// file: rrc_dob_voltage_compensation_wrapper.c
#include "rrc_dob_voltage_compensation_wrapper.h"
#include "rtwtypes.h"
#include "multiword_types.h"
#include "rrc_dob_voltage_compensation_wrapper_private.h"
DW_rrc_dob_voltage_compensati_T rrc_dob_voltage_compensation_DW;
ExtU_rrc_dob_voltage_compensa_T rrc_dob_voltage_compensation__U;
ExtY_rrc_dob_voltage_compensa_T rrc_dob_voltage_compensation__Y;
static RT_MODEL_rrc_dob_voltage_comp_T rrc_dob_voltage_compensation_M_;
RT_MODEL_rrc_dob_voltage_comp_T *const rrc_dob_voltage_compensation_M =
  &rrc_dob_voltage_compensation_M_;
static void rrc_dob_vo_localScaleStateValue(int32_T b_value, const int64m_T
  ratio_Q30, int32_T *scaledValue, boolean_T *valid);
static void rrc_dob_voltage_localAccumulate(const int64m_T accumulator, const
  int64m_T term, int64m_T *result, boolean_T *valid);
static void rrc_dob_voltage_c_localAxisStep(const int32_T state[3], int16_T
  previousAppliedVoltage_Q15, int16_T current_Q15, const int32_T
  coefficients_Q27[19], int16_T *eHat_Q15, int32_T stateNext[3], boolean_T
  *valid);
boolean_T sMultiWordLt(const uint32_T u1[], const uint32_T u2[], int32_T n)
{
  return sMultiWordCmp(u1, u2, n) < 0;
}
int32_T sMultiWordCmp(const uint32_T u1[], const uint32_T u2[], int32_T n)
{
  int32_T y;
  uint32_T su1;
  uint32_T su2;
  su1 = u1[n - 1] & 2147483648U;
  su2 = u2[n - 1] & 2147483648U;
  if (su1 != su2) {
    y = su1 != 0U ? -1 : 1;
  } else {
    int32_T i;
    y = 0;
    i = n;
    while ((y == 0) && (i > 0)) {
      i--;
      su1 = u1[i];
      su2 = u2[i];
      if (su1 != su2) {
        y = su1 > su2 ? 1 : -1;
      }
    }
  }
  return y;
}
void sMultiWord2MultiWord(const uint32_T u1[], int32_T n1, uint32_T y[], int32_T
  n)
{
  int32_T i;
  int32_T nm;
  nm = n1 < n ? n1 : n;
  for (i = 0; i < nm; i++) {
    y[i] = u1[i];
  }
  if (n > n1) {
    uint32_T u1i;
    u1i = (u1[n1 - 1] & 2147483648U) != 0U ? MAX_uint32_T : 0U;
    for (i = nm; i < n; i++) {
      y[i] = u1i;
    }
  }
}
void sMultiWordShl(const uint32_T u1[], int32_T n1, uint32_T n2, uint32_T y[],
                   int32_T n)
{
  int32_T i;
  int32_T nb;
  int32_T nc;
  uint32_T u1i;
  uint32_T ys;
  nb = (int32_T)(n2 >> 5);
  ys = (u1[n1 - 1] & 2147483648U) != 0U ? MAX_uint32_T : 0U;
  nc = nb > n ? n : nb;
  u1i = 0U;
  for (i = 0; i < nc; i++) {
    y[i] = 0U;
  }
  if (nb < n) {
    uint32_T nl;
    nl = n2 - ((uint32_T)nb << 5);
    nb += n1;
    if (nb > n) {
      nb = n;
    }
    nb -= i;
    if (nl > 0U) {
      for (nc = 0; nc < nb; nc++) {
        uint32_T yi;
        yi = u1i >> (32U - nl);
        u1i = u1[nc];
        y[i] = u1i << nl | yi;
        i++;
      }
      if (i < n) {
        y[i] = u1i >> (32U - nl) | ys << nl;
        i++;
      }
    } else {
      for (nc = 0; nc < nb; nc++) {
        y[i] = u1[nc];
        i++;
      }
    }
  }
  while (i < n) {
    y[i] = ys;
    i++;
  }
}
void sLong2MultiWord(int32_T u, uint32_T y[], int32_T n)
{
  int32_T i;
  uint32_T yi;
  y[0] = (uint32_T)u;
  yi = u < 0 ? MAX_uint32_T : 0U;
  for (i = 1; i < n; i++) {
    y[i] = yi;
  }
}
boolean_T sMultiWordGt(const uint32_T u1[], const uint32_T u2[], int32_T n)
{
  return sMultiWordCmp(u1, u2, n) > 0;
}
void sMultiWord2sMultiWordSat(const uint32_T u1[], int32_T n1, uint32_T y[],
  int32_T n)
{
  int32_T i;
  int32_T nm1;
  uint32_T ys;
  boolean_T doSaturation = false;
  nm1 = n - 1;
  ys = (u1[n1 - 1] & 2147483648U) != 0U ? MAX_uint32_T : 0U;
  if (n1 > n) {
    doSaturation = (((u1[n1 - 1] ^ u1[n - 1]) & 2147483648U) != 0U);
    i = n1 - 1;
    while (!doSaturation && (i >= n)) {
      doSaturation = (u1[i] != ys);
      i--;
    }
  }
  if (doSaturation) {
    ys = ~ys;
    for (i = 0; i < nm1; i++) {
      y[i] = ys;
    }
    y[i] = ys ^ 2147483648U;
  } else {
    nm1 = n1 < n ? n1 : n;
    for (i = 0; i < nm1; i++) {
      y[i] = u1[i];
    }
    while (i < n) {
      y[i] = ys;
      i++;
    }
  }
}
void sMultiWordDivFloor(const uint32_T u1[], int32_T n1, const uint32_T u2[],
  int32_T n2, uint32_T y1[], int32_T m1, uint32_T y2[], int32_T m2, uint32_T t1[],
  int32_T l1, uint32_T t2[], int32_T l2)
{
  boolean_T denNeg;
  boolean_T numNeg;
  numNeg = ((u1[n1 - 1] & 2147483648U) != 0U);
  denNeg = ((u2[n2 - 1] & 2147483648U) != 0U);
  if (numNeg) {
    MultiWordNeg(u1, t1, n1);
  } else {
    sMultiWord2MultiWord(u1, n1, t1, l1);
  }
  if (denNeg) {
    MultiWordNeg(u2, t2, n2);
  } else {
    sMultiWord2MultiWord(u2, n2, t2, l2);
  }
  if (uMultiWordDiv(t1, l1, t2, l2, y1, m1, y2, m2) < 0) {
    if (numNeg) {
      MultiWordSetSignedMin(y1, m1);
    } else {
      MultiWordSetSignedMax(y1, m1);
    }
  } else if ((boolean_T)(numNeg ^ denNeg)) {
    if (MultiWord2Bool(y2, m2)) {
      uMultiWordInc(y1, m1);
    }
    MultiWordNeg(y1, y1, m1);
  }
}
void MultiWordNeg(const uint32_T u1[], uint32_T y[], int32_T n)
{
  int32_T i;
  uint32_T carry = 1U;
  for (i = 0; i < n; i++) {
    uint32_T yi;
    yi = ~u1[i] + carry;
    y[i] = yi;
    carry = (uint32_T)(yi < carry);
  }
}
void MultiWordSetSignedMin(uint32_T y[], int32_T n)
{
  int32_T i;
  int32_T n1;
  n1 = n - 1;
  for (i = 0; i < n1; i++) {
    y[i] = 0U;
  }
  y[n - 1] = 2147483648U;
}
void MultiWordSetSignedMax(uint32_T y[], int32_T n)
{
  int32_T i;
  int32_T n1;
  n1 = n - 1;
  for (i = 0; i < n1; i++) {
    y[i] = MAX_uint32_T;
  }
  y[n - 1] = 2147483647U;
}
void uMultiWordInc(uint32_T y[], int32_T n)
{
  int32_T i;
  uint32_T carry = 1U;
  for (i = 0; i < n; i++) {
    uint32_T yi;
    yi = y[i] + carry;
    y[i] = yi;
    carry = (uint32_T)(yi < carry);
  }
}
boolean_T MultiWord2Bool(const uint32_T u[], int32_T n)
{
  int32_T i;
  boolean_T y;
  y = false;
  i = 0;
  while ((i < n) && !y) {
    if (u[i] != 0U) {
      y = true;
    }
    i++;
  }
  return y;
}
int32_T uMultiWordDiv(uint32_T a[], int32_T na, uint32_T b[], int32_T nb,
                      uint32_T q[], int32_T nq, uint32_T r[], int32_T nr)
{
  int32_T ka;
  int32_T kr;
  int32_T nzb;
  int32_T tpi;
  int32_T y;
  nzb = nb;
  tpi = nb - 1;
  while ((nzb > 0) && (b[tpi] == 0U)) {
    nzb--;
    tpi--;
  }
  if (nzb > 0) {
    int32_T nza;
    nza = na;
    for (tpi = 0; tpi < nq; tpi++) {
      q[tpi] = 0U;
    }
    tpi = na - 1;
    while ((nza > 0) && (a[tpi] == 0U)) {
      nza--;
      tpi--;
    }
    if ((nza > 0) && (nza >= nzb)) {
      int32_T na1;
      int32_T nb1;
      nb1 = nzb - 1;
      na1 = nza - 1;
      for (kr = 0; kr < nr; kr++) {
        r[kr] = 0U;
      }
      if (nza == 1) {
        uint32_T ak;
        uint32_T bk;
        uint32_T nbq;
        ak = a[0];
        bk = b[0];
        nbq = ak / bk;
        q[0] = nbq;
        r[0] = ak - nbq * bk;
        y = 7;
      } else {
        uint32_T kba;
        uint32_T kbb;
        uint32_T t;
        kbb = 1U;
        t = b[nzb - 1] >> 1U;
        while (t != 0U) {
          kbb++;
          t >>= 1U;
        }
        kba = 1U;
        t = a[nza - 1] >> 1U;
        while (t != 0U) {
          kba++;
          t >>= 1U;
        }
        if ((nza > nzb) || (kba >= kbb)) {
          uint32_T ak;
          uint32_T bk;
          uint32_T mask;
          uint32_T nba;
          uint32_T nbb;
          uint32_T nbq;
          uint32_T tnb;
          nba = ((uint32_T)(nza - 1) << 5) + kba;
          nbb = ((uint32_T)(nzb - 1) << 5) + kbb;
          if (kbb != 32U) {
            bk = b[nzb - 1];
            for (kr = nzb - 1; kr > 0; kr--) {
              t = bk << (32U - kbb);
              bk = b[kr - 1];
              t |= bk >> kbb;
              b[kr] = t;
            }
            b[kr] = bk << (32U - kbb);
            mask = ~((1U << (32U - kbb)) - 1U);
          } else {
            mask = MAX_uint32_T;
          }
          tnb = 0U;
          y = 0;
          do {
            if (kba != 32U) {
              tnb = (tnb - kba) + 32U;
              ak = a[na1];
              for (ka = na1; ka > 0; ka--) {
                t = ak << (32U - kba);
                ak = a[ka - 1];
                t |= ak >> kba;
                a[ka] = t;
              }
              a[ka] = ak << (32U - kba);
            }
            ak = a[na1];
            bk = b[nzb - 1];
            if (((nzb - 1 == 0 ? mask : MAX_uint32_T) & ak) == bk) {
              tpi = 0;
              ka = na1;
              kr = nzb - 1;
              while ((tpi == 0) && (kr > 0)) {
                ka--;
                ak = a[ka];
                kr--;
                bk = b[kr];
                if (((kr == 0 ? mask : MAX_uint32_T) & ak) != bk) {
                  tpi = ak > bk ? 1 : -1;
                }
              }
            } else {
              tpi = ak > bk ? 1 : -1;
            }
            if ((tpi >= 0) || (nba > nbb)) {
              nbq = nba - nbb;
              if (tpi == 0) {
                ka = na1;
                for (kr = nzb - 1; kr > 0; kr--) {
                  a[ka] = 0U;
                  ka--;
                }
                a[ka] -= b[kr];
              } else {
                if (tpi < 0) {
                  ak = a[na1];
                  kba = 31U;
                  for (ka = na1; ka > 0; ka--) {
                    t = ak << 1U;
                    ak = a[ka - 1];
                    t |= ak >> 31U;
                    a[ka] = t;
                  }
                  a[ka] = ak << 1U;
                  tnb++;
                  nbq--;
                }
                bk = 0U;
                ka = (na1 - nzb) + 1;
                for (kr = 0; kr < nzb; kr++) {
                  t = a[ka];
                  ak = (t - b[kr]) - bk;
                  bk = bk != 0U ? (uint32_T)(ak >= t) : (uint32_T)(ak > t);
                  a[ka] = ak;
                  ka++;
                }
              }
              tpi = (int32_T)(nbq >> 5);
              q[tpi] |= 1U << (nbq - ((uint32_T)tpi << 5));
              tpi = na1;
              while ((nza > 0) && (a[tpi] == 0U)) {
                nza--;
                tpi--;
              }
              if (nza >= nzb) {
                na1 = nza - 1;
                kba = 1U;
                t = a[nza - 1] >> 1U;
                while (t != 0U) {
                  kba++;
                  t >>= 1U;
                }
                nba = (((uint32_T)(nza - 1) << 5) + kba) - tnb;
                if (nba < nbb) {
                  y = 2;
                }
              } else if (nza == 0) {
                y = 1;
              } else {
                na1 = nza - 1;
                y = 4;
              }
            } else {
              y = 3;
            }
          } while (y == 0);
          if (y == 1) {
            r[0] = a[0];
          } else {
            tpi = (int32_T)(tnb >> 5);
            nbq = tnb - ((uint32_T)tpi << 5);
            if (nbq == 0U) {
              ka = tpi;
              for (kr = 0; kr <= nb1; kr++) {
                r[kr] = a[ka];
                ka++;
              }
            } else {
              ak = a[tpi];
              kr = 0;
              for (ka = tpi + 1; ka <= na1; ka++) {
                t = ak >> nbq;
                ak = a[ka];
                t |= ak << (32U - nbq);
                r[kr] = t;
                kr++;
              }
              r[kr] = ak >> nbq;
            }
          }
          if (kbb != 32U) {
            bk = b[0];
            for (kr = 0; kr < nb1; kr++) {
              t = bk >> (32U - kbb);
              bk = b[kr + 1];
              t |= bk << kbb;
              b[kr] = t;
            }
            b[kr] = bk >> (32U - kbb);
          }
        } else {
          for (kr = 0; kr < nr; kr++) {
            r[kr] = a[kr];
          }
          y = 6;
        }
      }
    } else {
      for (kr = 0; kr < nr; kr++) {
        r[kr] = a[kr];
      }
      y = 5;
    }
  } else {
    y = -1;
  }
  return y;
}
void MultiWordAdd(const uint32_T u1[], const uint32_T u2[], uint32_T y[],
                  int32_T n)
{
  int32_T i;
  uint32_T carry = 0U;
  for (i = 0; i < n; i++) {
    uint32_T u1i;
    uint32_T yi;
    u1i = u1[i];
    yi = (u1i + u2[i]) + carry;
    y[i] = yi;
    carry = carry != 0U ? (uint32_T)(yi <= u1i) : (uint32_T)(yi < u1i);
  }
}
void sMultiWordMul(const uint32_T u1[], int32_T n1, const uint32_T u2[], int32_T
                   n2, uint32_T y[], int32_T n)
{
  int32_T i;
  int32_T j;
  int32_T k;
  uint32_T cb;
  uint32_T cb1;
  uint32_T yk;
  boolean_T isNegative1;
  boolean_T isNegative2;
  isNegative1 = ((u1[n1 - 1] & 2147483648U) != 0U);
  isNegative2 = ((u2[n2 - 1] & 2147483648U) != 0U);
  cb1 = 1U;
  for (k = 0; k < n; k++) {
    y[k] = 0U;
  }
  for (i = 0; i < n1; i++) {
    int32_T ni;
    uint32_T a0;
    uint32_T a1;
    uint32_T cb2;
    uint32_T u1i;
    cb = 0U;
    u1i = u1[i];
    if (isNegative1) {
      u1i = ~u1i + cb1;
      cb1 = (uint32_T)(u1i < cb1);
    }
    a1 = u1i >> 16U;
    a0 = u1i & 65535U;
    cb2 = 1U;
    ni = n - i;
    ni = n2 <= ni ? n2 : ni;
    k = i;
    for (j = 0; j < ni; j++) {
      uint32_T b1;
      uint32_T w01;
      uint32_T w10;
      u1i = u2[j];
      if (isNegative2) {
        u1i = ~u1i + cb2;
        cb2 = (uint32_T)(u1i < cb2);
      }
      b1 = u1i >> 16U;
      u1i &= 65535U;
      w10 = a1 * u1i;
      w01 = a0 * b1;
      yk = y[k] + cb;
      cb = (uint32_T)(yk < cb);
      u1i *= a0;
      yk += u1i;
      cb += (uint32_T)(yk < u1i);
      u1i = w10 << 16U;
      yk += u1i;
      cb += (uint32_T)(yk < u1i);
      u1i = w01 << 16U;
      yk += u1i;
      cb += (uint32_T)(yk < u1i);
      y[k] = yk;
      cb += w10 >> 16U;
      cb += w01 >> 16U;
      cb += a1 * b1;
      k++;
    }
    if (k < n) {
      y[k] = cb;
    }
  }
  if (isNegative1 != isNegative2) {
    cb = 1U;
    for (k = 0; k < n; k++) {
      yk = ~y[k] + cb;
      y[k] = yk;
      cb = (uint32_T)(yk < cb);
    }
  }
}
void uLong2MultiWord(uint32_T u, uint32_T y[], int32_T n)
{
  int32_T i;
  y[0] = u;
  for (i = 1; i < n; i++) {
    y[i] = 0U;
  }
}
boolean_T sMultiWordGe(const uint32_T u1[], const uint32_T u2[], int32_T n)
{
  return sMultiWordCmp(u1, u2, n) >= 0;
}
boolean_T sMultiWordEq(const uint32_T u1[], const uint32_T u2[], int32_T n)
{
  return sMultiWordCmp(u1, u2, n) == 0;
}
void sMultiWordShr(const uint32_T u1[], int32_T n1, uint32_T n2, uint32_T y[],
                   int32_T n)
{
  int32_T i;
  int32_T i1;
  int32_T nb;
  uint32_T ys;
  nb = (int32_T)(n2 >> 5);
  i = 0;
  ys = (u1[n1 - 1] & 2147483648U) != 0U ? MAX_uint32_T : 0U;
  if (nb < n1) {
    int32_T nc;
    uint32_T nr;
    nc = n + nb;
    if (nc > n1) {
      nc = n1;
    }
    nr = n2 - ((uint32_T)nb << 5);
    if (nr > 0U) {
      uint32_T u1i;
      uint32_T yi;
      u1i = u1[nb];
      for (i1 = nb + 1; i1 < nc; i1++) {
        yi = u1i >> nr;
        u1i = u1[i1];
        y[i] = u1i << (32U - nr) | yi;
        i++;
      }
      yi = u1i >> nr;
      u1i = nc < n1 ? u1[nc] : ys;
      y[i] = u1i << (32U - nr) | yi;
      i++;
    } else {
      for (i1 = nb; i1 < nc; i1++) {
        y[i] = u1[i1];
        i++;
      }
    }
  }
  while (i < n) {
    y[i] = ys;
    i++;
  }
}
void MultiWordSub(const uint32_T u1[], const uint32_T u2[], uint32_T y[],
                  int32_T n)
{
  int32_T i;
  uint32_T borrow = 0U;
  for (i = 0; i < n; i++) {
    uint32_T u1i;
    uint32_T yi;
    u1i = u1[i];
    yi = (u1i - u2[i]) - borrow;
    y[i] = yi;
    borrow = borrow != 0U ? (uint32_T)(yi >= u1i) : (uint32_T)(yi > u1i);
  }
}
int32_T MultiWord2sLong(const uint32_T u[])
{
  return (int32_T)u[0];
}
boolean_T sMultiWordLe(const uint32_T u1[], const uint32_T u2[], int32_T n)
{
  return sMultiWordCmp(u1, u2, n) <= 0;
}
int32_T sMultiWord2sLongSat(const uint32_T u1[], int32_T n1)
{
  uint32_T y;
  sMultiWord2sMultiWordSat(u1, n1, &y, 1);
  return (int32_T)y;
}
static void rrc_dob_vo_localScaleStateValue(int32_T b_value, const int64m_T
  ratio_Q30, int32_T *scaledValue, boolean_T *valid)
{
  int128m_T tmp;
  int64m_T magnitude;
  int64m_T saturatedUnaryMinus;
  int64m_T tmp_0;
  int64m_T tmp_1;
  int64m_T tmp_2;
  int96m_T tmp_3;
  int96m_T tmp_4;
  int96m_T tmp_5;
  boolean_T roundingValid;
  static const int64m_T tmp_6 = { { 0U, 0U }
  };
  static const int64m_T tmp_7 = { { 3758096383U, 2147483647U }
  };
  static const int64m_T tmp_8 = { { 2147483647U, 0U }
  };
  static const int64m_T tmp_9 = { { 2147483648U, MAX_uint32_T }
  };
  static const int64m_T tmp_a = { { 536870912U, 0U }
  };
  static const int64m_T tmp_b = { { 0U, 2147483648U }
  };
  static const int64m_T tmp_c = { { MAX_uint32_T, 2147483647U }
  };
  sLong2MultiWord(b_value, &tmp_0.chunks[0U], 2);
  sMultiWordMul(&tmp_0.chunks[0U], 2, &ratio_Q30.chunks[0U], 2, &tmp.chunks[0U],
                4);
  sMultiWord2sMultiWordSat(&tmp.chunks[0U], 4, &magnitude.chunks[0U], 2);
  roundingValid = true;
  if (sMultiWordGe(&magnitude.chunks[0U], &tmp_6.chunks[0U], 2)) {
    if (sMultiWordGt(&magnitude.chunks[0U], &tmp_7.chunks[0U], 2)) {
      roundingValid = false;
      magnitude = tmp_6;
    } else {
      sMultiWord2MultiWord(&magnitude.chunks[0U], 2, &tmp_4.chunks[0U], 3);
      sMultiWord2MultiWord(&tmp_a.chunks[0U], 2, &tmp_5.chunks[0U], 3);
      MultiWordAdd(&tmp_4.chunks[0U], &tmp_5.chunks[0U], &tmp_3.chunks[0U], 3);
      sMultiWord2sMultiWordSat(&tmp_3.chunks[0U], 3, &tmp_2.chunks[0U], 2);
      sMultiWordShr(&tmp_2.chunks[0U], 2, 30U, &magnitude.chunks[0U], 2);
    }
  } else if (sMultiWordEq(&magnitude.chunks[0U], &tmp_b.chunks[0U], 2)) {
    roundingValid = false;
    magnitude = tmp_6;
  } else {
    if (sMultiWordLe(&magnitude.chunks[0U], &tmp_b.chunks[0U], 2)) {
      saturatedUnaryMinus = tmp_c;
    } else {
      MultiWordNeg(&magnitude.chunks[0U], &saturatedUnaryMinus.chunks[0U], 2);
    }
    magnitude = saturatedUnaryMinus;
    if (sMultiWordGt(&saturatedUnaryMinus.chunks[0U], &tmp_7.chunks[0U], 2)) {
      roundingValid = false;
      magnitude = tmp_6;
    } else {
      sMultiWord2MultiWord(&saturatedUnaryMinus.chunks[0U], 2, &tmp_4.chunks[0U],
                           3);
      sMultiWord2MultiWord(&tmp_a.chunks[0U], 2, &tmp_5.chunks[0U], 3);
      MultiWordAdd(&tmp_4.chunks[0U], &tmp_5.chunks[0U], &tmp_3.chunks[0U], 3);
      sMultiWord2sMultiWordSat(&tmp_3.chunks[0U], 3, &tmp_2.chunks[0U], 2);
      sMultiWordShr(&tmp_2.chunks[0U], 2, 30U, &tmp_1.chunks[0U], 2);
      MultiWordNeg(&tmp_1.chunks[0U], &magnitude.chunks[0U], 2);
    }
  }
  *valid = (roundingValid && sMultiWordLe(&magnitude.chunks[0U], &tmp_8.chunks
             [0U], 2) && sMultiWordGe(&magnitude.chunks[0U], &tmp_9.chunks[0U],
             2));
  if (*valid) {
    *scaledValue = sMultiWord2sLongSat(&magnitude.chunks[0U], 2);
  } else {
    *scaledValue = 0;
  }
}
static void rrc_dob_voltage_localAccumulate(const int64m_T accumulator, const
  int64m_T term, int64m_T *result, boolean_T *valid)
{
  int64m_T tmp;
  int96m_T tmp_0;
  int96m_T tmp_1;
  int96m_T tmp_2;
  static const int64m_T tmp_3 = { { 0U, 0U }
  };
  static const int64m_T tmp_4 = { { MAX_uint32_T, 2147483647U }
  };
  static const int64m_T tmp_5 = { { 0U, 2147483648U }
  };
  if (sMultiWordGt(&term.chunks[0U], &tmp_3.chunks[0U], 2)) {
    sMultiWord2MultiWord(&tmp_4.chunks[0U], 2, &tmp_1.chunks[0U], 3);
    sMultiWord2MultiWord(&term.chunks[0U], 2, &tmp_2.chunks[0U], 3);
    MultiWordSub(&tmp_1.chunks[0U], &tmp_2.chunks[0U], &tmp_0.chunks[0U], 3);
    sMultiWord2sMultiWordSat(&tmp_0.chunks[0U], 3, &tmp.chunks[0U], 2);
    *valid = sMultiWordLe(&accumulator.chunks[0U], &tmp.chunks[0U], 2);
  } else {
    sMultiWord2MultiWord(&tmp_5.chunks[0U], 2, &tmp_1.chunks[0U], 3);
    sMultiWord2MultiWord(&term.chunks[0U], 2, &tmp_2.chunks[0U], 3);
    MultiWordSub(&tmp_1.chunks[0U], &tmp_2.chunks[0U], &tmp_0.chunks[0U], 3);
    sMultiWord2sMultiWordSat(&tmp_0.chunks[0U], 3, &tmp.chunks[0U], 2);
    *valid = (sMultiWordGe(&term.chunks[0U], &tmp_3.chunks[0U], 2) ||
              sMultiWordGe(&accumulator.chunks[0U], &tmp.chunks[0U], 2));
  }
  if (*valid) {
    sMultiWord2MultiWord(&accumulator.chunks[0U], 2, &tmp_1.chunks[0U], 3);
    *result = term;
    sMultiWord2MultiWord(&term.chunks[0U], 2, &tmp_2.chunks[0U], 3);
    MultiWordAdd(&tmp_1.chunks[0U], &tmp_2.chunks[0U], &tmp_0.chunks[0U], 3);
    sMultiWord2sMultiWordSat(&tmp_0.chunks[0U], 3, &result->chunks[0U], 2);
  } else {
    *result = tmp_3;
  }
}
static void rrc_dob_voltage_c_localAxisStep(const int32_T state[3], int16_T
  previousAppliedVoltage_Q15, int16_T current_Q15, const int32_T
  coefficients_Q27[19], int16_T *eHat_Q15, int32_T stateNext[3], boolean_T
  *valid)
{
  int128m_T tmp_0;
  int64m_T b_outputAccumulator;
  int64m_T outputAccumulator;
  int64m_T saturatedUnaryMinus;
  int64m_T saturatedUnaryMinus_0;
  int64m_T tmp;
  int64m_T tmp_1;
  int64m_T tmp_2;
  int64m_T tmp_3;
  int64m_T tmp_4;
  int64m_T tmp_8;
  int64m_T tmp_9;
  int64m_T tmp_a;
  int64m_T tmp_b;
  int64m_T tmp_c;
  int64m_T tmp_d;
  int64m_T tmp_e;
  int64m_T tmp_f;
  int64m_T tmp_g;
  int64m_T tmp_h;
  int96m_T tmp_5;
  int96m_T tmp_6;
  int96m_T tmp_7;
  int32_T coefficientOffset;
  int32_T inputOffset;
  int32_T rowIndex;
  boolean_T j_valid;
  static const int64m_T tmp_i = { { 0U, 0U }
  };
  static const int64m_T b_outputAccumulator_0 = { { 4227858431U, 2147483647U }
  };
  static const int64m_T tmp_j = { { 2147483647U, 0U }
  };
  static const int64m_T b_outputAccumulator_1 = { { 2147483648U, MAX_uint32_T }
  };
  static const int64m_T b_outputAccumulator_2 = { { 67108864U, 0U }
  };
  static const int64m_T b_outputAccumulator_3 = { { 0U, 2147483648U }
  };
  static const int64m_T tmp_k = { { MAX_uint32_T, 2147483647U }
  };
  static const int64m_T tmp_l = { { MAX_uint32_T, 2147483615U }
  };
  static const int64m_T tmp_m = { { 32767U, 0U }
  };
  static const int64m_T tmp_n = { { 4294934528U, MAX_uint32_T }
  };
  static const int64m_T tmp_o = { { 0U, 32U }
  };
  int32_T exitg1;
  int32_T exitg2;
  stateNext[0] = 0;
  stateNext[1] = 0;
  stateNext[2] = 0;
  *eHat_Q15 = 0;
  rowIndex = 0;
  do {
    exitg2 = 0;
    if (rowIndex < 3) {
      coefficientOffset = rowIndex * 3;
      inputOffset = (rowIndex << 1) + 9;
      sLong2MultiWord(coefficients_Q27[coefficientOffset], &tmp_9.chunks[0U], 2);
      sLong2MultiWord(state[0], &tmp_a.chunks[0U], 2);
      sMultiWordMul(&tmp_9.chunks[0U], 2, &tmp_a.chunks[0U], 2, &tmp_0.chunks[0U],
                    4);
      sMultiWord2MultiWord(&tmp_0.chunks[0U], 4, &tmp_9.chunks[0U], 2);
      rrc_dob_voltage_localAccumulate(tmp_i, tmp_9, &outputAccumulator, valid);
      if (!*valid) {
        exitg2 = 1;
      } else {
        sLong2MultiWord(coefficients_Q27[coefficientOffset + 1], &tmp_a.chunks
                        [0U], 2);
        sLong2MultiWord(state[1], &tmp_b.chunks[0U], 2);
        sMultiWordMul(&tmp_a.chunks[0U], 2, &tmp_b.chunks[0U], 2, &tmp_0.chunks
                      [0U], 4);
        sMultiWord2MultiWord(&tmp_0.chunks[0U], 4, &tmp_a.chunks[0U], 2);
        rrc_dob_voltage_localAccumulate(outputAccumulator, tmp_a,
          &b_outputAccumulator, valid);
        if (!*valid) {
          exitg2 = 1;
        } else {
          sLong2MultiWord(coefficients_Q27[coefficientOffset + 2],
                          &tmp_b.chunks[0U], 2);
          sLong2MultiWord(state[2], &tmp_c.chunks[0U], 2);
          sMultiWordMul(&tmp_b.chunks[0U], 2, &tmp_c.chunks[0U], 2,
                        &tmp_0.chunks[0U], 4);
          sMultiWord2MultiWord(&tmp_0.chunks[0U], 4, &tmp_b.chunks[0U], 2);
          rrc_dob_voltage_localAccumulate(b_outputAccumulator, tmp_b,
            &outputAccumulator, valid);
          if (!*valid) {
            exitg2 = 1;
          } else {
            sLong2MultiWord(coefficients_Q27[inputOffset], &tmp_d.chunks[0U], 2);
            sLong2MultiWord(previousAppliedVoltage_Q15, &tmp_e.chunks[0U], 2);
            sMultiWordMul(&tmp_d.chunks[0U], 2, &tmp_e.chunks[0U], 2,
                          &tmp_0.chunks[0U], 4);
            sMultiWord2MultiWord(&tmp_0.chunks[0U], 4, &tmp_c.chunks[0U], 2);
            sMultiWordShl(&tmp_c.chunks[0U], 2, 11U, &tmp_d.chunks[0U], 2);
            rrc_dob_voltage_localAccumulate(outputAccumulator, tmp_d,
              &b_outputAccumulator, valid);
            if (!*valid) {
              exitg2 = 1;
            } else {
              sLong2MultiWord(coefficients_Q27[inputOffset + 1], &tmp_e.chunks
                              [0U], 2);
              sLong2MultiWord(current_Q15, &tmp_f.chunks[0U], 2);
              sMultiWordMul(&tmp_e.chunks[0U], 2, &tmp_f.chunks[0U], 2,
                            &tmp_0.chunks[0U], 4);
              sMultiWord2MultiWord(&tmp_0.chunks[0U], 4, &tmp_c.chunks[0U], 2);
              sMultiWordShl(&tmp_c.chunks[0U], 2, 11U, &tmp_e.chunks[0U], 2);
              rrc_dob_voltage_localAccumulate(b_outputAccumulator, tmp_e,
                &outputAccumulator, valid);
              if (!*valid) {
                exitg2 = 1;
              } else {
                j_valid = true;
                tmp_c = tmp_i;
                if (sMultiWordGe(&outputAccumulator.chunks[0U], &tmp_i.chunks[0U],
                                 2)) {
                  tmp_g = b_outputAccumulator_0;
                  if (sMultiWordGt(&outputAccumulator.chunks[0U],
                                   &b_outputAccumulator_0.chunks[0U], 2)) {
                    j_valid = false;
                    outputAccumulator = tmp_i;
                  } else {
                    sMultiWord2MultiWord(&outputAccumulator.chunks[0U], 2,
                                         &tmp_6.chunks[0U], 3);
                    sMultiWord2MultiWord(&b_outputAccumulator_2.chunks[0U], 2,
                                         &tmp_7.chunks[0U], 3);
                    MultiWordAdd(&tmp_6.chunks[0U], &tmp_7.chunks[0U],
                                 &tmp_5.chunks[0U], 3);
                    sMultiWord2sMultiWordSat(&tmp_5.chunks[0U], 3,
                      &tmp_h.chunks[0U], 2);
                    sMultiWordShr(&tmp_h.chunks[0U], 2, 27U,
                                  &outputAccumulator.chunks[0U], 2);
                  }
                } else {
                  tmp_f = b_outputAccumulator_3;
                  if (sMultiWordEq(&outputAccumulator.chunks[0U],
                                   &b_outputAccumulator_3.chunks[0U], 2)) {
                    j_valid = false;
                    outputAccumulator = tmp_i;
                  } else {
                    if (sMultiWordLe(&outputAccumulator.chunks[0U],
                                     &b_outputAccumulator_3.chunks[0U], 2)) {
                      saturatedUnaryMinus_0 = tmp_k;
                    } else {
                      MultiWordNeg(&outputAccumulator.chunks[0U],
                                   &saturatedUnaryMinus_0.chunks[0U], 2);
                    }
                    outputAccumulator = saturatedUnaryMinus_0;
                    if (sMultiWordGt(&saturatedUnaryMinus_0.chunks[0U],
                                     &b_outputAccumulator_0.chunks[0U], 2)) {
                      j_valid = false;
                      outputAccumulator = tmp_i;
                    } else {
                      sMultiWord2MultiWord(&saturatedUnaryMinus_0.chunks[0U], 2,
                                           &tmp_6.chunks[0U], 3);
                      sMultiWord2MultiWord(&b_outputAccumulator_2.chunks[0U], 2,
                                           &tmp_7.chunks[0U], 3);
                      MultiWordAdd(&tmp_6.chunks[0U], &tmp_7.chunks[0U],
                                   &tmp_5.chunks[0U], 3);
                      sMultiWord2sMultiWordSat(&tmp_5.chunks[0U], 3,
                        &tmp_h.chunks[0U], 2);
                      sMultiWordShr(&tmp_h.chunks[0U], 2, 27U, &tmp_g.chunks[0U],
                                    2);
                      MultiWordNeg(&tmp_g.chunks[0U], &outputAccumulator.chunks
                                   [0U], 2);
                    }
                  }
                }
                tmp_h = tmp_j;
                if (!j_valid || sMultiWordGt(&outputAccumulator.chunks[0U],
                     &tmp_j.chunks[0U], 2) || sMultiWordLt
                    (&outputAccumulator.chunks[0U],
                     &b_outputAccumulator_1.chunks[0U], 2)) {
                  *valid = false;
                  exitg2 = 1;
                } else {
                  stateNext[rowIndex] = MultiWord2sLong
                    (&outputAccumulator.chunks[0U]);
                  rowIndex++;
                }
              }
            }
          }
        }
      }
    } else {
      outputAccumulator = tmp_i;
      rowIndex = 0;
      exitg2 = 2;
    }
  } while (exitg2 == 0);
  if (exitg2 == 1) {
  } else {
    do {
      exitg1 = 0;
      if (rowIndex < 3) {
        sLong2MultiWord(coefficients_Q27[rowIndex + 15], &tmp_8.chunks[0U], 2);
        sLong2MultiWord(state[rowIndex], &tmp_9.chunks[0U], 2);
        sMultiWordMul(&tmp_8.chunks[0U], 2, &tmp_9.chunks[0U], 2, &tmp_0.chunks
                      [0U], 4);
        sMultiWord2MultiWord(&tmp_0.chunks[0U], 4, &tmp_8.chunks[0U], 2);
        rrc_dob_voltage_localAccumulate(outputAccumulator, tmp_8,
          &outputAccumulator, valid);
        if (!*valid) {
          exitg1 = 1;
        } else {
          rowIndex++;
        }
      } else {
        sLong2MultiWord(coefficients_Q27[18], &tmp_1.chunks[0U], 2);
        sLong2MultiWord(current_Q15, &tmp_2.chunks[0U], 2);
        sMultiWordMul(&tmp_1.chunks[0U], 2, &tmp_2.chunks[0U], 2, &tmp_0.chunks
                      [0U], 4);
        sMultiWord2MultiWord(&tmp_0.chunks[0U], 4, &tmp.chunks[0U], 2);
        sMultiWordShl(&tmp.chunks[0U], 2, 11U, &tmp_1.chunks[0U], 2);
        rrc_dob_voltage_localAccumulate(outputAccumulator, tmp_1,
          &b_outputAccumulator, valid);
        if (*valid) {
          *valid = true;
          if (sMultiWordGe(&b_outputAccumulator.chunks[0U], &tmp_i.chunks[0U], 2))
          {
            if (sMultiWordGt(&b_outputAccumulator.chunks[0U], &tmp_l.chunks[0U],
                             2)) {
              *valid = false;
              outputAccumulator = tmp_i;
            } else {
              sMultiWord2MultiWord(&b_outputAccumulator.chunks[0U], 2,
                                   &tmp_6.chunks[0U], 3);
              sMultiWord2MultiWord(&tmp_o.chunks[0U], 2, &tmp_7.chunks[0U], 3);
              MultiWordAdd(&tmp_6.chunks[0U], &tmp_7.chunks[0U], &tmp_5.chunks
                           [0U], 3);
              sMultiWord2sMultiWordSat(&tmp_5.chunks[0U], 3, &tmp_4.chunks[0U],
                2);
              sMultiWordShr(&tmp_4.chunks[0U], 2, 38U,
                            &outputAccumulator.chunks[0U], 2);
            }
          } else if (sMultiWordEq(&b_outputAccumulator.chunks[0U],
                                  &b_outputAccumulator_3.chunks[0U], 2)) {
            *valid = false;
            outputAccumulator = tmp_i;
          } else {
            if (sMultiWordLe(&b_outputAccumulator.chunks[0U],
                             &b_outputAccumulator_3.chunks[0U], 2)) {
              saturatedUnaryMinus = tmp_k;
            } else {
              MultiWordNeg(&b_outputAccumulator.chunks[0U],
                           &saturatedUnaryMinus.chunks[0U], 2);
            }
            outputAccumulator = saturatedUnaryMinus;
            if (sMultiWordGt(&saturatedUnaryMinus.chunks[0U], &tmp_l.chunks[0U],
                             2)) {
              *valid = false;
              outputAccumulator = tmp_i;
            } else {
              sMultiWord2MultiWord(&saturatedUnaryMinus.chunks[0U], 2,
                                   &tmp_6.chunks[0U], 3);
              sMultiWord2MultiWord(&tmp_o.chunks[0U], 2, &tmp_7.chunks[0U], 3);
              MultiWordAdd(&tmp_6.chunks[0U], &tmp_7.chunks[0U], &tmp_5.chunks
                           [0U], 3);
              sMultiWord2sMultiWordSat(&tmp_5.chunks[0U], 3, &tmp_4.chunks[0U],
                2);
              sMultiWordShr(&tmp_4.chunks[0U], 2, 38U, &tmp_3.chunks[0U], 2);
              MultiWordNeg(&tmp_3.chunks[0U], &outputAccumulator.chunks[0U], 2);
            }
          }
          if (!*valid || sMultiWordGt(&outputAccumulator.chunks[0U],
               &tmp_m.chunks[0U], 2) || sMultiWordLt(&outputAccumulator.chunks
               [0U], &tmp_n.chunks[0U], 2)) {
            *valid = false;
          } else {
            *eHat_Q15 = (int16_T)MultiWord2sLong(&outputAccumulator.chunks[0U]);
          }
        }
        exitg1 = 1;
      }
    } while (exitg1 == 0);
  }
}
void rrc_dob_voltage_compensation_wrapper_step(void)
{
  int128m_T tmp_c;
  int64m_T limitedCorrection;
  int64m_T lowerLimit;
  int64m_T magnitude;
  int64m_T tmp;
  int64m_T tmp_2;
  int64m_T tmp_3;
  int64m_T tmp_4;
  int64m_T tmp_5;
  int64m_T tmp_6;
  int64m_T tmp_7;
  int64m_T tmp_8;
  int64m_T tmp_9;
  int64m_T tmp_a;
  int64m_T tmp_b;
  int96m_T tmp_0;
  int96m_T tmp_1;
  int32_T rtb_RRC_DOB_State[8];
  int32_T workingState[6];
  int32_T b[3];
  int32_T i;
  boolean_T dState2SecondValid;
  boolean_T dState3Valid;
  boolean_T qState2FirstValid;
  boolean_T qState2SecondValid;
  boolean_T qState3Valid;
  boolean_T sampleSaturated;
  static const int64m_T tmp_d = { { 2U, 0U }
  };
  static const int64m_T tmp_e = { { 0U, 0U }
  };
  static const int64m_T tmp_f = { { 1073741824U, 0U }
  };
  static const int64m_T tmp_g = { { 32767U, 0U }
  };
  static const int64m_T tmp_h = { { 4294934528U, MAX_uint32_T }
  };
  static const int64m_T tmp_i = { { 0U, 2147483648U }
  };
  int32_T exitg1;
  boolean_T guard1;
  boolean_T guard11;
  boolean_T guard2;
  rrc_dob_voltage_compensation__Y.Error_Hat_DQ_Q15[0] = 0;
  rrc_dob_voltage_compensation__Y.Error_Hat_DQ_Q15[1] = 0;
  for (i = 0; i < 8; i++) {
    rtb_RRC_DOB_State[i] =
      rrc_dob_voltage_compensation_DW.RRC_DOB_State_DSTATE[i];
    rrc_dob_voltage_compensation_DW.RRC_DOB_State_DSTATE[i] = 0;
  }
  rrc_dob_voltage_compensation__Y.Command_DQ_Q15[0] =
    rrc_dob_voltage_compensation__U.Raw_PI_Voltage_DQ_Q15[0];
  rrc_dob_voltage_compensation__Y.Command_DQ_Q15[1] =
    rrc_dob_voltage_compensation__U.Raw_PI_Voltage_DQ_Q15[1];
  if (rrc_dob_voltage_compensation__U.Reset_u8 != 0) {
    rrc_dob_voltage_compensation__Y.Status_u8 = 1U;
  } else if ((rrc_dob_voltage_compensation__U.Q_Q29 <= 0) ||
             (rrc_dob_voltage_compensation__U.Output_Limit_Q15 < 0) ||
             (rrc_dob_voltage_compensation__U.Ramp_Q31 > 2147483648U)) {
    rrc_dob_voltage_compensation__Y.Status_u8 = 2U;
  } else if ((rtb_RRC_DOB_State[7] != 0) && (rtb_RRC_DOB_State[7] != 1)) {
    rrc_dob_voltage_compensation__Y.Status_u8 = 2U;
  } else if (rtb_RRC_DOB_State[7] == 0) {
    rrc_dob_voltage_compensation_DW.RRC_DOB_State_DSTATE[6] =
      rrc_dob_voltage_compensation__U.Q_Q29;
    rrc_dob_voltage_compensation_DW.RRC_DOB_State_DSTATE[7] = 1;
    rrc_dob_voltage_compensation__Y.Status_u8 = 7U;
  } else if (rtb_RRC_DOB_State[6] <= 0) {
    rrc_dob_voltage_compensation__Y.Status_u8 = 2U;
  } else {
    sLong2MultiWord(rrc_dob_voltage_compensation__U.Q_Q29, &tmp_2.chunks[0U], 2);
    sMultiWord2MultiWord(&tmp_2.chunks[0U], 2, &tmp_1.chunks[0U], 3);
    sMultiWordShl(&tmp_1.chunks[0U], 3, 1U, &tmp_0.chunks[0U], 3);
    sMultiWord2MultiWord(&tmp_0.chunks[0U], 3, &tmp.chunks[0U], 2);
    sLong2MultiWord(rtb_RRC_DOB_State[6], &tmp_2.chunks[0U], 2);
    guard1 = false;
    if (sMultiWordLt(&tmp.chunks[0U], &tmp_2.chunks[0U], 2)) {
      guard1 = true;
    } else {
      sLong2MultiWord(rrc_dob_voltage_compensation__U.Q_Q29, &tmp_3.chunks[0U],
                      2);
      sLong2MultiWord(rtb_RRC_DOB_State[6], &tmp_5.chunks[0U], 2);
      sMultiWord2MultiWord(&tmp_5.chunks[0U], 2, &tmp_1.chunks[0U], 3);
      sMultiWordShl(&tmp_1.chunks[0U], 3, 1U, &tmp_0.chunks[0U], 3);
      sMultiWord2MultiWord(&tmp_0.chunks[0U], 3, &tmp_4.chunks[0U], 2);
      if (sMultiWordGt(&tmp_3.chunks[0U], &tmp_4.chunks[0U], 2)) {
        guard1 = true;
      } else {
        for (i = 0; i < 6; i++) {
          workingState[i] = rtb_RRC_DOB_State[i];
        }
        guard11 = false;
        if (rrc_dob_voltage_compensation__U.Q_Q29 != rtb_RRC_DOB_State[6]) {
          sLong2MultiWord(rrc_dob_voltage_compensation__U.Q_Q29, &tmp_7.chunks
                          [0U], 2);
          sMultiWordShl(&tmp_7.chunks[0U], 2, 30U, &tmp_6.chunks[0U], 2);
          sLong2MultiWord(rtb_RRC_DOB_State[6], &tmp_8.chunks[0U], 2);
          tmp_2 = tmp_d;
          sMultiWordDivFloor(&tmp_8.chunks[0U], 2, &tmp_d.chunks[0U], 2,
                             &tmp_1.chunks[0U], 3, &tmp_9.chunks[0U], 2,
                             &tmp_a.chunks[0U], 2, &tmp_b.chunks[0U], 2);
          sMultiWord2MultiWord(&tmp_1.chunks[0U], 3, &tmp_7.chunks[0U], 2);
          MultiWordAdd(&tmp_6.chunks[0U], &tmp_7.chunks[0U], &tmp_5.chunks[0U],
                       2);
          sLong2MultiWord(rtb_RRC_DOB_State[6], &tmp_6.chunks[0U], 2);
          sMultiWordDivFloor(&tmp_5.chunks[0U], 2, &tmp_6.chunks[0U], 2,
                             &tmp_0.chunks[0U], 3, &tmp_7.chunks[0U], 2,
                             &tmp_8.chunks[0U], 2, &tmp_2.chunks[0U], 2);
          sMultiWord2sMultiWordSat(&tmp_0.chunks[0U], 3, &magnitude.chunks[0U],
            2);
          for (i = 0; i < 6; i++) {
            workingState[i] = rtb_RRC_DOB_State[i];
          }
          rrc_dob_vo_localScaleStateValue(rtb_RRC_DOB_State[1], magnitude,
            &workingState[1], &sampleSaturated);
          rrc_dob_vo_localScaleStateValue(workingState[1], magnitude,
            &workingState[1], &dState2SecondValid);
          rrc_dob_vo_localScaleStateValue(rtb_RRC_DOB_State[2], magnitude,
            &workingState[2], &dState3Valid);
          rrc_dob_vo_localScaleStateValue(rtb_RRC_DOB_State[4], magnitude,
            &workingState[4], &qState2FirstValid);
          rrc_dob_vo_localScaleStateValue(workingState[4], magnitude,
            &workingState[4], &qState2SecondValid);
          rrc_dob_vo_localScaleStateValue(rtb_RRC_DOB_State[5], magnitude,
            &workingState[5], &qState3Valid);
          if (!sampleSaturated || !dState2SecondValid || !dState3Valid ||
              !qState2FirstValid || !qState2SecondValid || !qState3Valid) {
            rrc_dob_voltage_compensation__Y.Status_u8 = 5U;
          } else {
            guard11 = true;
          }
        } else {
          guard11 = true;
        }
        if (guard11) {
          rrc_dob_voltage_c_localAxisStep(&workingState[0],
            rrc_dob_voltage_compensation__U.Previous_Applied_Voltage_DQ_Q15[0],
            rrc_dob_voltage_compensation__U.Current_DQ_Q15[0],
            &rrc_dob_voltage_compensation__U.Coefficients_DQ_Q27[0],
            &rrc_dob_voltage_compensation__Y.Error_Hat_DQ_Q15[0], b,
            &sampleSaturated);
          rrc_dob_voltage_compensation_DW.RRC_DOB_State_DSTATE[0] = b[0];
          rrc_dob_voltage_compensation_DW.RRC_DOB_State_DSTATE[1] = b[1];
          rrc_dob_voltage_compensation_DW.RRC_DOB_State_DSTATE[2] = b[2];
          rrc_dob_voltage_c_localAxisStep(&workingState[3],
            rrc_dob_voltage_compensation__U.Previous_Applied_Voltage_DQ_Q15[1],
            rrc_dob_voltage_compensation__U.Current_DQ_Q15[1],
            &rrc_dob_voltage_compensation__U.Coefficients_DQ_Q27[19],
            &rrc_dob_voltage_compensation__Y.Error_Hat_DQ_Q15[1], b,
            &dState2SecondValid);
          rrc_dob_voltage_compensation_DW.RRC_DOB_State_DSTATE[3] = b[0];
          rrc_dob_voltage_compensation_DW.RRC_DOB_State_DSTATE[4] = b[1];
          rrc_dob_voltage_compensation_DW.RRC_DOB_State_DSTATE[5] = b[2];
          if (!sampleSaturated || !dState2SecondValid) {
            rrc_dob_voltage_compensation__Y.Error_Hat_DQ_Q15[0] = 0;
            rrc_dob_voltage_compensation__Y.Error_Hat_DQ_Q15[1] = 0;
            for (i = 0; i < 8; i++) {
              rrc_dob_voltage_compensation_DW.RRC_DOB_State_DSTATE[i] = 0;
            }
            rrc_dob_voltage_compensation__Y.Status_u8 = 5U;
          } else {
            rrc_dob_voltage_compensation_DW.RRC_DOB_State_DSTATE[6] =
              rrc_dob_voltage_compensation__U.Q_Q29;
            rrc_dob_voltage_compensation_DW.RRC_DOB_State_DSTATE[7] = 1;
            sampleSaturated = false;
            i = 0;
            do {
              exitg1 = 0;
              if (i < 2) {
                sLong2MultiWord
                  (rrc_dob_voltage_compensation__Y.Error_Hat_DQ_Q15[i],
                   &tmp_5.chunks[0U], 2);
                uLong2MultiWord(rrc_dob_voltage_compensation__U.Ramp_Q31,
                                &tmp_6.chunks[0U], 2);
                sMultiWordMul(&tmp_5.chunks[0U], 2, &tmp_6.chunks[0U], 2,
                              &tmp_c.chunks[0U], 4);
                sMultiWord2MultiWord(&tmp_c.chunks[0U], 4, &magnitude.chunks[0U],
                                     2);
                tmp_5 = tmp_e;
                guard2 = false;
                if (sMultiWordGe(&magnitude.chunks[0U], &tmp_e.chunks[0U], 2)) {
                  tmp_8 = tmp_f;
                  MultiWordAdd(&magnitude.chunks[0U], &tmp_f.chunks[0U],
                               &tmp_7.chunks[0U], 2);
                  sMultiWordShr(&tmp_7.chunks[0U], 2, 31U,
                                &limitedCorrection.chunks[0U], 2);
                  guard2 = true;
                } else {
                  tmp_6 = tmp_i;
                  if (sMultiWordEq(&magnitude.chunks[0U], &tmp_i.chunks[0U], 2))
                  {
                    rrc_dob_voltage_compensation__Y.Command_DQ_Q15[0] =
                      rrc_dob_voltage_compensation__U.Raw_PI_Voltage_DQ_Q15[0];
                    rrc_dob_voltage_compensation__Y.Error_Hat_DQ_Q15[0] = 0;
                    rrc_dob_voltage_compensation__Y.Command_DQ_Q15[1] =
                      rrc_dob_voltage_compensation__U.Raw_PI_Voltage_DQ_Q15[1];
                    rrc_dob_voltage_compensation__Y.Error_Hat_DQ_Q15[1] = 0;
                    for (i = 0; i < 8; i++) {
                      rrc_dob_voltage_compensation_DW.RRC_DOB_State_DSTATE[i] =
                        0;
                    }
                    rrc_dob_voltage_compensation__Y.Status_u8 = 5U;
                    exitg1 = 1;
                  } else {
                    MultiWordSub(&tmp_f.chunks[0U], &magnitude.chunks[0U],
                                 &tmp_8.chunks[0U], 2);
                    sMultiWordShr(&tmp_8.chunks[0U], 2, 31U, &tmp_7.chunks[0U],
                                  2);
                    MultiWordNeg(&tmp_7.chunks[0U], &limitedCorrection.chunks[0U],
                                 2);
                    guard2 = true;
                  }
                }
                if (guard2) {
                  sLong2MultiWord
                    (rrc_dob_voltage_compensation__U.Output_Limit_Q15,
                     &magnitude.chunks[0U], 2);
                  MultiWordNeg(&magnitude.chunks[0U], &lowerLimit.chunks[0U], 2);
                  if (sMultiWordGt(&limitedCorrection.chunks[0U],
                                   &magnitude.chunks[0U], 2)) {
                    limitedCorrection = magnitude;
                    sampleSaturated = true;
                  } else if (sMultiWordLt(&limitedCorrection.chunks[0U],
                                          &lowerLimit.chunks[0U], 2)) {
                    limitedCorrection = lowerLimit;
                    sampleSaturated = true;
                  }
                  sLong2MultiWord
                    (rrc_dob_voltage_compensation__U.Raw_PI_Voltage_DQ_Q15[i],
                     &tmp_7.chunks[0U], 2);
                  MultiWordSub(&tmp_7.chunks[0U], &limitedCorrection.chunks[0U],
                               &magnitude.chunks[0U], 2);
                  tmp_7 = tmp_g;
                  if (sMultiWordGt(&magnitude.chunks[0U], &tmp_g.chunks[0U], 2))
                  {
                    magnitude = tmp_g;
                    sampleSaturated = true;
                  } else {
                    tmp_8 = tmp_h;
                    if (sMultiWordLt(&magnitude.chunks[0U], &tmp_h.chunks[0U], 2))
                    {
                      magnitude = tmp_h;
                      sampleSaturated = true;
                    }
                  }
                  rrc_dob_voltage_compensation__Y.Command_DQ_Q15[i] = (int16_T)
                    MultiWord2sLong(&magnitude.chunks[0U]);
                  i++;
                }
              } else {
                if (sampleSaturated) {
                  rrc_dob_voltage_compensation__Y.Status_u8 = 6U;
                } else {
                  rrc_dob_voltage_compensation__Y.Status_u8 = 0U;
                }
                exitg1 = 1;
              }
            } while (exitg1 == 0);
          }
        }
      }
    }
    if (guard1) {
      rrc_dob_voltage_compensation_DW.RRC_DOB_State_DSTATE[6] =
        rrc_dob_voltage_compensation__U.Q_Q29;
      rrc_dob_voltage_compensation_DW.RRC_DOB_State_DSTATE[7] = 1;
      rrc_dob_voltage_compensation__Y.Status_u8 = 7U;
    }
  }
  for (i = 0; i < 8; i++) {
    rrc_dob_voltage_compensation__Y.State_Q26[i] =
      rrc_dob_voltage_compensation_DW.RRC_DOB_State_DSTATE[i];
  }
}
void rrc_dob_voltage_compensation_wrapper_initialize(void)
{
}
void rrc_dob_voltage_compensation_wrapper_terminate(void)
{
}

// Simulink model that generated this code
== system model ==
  Previous_Applied_Voltage_DQ_Q15 : Inport
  Current_DQ_Q15 : Inport
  Raw_PI_Voltage_DQ_Q15 : Inport
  Coefficients_DQ_Q27 : Inport
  Q_Q29 : Inport
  Reset_u8 : Inport
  Ramp_Q31 : Inport
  Output_Limit_Q15 : Inport
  Command_DQ_Q15 : Outport  <- 1: MATLABFunction#1
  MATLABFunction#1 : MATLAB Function  <- 1: RRC_DOB_State, 2: Previous_Applied_Voltage_DQ_Q15, 3: Current_DQ_Q15, 4: Raw_PI_Voltage_DQ_Q15, 5: Coefficients_DQ_Q27, 6: Q_Q29, 7: Reset_u8, 8: Ramp_Q31, 9: Output_Limit_Q15
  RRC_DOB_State : UnitDelay  InitialCondition=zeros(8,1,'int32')  <- 1: MATLABFunction#1/3
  Error_Hat_DQ_Q15 : Outport  <- 1: MATLABFunction#1/2
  State_Q26 : Outport  <- 1: MATLABFunction#1/3
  Status_u8 : Outport  <- 1: MATLABFunction#1/4
== matlab function MATLABFunction#1 ==
function [commandDQ_Q15, eHatDQ_Q15, stateNext, status] = RRC_DOB_FixedStep(state, previousAppliedVoltageDQ_Q15, currentDQ_Q15, rawPiVoltageDQ_Q15, coefficientsDQ_Q27, q_Q29, reset, ramp_Q31, outputLimit_Q15)
%#codegen
[commandDQ_Q15, eHatDQ_Q15, stateNext, status] = rrcDobFixedPointStep(state, previousAppliedVoltageDQ_Q15, currentDQ_Q15, rawPiVoltageDQ_Q15, coefficientsDQ_Q27, q_Q29, reset, ramp_Q31, outputLimit_Q15);
end
